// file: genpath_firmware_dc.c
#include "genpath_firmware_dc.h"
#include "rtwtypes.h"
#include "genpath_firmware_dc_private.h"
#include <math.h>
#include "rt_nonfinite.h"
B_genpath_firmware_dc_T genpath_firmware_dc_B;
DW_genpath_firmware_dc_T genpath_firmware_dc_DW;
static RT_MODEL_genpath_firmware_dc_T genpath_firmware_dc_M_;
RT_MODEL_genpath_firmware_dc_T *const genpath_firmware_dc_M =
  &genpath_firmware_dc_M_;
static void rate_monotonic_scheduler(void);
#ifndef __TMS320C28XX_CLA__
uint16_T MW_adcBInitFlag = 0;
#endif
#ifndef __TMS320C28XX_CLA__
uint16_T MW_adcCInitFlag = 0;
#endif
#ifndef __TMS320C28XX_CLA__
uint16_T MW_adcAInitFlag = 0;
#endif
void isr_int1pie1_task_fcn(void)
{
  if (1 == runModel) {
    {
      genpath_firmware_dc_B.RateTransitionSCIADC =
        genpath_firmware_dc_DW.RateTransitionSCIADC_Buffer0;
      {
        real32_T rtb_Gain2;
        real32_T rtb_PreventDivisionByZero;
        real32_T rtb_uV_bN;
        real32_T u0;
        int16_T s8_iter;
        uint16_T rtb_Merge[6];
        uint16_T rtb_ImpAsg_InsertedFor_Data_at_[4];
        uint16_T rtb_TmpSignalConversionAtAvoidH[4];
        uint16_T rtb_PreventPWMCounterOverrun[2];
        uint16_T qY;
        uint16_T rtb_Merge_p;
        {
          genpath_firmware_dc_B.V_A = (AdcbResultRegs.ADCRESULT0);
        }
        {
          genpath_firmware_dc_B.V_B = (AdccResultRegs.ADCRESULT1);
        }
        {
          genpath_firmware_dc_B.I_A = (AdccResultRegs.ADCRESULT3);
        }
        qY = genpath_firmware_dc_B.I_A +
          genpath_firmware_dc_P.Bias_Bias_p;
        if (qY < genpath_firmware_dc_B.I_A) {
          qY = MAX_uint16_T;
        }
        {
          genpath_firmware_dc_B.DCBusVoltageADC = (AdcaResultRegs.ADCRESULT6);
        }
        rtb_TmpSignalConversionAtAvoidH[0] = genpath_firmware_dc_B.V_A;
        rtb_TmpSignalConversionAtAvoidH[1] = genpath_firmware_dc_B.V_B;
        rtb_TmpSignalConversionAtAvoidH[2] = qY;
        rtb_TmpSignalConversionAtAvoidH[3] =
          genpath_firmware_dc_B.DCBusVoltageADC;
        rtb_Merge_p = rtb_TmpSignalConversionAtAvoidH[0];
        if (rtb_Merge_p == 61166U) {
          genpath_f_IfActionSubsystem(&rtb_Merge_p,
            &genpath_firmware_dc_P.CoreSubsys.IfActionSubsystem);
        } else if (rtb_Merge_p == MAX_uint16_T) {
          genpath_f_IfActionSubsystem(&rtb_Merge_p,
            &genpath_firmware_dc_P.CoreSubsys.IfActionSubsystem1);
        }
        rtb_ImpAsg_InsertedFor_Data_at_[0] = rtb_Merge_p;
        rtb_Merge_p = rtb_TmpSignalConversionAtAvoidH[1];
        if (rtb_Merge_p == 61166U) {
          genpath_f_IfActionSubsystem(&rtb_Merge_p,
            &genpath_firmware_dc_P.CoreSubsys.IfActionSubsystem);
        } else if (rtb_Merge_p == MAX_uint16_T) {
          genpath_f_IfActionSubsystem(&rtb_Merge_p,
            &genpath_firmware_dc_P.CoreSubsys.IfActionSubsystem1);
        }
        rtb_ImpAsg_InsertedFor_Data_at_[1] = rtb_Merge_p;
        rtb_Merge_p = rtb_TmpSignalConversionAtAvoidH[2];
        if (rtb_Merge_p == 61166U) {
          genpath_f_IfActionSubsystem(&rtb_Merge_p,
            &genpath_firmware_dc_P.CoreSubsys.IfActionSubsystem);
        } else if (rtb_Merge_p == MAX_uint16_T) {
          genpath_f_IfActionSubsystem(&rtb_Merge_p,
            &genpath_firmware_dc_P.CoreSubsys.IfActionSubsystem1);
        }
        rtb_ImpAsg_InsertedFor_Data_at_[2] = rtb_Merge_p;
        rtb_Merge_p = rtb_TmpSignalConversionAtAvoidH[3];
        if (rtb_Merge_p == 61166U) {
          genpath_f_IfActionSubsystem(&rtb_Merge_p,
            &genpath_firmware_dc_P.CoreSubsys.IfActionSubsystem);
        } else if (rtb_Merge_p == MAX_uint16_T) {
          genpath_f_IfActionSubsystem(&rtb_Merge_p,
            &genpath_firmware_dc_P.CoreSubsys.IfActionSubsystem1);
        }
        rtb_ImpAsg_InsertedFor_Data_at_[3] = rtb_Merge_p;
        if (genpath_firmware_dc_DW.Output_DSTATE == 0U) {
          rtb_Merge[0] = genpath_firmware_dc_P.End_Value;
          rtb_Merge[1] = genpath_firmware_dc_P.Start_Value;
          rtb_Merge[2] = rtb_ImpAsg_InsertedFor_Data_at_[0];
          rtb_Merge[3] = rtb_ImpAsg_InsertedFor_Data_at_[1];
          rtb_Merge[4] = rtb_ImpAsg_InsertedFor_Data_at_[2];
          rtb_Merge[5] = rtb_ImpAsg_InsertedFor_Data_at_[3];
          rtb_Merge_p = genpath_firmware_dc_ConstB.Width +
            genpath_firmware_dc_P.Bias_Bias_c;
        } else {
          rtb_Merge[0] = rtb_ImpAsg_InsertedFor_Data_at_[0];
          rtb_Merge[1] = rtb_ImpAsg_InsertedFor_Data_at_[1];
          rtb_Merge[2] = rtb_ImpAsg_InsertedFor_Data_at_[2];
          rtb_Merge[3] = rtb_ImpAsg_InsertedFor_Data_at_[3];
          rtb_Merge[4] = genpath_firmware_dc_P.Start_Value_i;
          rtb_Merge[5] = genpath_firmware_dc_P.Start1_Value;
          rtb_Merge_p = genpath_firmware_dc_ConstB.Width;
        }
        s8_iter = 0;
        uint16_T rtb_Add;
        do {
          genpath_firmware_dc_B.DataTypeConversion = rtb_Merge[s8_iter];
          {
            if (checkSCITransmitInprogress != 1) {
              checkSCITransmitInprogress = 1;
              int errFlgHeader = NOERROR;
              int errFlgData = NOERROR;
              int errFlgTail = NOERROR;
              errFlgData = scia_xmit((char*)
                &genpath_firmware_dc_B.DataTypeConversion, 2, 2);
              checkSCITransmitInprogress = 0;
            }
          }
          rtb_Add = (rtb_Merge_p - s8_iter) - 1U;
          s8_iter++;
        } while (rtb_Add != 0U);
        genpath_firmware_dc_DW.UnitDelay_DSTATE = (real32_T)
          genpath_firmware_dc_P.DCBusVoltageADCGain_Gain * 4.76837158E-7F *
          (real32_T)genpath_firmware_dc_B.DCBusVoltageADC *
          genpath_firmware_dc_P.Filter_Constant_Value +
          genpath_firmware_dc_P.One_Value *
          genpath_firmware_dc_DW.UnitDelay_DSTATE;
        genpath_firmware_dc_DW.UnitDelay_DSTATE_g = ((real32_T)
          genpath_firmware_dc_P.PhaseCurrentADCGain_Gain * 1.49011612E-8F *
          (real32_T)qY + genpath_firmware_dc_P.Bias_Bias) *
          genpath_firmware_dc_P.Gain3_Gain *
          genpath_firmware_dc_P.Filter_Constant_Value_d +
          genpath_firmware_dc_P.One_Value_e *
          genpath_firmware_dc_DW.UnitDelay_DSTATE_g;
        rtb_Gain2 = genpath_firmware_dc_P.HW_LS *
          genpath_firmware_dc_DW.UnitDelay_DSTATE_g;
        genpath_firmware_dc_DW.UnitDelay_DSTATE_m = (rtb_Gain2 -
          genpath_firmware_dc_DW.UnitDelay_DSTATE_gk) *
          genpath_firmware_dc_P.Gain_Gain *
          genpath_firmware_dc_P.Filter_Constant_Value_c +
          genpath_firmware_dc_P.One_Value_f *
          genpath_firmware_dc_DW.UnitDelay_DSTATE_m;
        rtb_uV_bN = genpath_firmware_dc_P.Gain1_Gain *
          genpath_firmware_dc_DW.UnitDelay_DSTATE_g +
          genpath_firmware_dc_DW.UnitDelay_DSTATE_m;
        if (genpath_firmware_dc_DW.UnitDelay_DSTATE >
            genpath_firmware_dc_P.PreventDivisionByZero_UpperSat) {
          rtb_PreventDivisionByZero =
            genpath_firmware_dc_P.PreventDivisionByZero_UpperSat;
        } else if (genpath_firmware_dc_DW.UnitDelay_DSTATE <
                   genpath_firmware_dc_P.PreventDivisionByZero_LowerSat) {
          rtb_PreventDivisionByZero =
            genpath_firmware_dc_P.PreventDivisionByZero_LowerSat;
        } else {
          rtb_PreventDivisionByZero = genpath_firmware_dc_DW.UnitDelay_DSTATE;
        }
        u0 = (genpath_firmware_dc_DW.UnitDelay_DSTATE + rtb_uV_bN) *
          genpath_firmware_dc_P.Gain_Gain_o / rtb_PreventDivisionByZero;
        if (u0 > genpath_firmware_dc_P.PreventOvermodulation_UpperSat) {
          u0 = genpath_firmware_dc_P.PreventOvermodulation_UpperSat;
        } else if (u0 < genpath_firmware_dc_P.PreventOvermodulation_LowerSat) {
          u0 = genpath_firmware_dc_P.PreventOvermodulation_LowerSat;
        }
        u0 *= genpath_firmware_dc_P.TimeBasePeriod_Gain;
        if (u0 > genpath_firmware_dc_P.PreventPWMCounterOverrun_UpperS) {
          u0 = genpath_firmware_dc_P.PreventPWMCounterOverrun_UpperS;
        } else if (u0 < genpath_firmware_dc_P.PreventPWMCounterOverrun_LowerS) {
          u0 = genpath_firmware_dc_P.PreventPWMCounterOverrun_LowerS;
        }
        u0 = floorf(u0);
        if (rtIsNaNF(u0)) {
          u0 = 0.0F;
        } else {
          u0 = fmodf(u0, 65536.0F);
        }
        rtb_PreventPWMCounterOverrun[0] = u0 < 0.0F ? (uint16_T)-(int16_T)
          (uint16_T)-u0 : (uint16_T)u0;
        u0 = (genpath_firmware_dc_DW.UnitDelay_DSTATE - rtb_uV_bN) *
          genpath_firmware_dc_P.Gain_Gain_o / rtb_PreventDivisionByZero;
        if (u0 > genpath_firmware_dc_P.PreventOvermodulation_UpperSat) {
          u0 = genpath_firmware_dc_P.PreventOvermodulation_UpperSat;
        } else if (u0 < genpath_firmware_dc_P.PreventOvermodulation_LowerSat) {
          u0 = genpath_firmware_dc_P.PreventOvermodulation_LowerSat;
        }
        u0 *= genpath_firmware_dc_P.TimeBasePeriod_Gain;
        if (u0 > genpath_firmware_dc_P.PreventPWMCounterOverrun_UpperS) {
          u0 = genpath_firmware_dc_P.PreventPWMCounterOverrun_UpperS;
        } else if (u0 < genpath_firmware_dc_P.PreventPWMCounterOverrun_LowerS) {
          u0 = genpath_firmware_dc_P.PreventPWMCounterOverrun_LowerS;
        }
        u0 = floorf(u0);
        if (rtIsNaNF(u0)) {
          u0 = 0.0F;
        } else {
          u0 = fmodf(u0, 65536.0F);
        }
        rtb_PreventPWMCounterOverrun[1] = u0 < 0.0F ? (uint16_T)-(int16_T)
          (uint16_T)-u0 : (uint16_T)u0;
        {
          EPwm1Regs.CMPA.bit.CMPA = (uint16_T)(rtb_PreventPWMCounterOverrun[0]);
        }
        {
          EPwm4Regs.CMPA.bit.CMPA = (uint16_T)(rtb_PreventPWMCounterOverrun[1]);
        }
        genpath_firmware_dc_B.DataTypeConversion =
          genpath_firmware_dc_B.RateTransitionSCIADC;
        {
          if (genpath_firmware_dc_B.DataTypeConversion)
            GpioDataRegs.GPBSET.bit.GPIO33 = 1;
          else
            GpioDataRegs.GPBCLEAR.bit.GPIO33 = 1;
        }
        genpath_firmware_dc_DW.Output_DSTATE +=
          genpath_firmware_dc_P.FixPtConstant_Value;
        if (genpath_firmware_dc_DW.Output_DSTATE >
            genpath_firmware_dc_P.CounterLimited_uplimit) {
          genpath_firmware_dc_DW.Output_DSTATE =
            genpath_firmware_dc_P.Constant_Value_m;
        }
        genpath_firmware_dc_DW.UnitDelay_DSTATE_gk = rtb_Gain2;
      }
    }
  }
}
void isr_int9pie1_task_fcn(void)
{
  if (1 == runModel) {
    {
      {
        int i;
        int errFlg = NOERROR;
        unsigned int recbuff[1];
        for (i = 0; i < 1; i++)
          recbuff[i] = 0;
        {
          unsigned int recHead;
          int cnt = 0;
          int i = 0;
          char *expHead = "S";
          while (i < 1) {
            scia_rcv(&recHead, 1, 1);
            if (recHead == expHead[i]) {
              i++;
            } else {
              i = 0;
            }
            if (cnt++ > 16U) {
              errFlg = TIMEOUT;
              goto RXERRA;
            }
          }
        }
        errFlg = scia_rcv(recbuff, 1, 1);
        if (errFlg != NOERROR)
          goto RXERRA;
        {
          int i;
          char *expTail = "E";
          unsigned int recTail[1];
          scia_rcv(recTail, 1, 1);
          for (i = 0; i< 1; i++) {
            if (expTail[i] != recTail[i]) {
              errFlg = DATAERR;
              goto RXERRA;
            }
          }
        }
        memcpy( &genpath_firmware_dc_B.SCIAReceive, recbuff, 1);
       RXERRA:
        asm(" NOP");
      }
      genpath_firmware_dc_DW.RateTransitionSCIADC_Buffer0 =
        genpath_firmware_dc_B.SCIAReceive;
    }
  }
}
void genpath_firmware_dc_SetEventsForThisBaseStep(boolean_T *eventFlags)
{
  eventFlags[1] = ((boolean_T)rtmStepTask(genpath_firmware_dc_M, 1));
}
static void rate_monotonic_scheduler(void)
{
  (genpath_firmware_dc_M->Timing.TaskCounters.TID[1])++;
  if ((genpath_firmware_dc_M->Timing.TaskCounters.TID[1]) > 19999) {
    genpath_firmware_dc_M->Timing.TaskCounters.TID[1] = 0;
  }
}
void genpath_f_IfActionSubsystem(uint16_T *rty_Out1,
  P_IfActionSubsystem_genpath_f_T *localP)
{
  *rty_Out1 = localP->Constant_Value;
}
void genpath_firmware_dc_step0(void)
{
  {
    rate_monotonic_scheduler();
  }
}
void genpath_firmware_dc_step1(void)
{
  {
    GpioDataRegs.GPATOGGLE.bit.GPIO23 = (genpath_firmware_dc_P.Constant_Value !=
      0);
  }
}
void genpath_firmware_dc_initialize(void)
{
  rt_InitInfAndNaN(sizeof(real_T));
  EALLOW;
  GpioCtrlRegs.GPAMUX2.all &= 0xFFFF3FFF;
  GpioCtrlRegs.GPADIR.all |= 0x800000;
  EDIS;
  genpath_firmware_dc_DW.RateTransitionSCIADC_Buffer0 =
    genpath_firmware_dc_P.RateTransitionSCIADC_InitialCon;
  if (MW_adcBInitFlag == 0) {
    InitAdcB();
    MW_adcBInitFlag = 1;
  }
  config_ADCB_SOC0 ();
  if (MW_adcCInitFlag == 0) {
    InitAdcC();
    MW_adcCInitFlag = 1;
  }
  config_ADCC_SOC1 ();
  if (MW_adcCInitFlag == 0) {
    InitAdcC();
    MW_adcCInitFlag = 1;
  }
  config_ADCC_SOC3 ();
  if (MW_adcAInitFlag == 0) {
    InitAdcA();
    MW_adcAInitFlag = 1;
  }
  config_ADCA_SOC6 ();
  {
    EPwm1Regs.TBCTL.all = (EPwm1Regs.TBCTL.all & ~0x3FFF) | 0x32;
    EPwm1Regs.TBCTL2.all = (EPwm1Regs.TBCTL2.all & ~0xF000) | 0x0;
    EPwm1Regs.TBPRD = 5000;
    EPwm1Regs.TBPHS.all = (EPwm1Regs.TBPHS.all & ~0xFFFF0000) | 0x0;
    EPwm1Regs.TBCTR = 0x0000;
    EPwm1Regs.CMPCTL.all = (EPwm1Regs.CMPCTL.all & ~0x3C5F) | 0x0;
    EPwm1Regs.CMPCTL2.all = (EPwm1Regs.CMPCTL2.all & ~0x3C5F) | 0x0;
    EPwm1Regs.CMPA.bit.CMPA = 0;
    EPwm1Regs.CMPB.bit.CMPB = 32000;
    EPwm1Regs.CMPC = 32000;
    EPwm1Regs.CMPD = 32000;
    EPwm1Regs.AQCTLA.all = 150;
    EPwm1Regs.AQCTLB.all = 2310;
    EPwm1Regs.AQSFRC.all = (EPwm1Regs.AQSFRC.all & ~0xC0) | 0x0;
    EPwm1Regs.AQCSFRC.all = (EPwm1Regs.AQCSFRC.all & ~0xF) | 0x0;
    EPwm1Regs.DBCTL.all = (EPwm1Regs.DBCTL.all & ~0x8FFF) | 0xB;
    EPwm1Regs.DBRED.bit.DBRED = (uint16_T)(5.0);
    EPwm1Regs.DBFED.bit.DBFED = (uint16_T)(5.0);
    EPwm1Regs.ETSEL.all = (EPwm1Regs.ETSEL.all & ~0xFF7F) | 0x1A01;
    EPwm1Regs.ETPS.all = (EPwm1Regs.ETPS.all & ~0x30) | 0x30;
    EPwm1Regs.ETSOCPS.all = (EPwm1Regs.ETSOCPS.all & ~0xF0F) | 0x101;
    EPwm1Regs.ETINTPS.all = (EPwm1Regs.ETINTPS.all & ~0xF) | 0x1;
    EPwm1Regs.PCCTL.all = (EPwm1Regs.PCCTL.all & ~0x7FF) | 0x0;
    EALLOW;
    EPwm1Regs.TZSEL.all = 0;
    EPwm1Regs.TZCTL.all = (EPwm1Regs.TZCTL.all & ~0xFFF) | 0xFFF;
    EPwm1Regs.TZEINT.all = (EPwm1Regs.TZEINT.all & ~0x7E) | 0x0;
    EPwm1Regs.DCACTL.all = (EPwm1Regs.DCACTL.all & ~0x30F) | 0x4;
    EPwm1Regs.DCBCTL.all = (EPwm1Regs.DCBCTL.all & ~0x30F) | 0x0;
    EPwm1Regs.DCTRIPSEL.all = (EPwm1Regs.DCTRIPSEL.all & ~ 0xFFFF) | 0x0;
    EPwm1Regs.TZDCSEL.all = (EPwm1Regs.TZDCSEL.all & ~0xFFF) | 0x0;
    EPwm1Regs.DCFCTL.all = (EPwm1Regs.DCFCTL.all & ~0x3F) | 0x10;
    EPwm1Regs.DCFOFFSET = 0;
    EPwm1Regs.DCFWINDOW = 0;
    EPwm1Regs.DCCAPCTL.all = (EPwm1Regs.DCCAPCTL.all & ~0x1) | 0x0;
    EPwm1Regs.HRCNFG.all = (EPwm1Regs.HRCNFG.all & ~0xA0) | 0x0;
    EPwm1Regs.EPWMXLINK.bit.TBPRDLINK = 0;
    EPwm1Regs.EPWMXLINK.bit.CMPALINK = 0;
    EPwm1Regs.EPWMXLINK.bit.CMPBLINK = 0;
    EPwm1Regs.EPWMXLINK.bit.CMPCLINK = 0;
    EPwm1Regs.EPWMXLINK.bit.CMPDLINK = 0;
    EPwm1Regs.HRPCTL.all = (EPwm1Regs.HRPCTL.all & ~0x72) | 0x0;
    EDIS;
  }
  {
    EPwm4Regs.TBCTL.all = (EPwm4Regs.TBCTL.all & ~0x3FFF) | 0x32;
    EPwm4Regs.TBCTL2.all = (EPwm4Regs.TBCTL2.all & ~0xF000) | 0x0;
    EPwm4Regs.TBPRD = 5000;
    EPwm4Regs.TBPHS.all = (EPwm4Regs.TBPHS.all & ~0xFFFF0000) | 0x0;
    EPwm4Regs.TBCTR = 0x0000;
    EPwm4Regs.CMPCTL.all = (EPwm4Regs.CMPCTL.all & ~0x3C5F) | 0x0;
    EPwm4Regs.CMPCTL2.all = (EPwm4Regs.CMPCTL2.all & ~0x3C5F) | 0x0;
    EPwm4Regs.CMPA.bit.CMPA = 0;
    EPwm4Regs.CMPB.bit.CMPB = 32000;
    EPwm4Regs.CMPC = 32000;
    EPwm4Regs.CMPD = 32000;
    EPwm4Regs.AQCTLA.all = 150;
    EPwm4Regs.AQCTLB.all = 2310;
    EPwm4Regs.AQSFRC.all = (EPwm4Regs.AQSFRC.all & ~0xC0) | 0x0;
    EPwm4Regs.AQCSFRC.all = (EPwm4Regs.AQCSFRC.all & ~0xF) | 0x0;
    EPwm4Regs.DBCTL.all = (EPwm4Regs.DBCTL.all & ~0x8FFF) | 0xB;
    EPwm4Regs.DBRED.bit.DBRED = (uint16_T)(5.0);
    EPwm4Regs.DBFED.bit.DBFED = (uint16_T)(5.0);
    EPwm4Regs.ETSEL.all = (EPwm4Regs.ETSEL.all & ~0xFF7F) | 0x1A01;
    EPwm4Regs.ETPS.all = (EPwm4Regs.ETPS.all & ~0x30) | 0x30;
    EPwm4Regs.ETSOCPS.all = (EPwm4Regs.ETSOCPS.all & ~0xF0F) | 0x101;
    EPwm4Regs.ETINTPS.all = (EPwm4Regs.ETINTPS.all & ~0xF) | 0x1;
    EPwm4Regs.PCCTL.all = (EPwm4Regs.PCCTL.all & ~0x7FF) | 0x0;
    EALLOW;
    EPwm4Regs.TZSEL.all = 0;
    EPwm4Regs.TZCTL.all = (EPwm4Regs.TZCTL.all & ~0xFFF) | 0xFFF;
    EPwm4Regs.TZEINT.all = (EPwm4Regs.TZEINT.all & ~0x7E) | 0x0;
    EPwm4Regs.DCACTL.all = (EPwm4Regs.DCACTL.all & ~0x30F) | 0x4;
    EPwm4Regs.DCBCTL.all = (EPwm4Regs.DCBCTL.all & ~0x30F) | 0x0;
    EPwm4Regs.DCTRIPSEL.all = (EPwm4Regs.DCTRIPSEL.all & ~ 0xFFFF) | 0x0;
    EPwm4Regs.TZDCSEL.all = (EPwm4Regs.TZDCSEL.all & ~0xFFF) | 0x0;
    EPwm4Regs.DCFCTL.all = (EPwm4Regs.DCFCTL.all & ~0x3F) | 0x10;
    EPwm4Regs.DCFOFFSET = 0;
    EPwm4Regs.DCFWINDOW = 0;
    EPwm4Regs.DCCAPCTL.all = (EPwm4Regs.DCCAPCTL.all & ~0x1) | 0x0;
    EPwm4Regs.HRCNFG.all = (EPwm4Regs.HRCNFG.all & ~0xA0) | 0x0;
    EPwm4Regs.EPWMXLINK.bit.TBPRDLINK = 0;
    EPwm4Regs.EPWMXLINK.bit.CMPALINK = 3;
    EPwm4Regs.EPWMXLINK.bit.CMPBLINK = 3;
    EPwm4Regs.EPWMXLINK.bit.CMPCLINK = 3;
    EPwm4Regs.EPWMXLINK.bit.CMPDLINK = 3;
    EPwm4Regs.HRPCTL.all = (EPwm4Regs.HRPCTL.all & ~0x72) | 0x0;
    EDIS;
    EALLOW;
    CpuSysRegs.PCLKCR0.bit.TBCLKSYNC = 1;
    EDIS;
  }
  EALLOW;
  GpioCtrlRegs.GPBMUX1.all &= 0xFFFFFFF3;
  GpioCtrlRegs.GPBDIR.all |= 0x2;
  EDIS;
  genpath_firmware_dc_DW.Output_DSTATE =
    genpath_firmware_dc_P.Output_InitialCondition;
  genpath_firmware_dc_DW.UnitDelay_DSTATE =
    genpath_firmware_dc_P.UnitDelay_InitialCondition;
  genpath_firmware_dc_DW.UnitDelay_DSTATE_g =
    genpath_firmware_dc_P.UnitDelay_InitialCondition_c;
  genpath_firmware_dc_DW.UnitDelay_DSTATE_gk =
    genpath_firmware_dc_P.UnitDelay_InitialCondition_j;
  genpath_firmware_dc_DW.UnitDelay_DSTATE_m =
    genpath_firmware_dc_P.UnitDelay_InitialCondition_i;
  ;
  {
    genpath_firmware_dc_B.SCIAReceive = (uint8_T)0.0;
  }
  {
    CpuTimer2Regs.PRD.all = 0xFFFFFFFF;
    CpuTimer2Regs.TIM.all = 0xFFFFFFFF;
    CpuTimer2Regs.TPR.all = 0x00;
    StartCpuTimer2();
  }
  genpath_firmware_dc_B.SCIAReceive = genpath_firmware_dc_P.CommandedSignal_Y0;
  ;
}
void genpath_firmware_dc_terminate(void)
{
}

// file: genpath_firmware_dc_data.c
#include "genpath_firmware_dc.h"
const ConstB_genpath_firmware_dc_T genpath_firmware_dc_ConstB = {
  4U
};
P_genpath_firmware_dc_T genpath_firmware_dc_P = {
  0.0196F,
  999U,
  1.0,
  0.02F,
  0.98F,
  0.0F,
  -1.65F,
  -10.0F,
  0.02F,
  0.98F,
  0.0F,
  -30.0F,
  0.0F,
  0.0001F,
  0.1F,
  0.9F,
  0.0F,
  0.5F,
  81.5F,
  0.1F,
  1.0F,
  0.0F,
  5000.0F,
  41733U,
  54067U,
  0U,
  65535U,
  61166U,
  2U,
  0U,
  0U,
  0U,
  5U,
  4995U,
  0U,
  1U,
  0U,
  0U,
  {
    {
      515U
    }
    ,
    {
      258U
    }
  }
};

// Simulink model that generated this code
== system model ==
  Subsystem#1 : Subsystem  <- 1: RateTransitionSCIADC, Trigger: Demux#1
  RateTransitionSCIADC : RateTransition  <- 1: Subsystem#2
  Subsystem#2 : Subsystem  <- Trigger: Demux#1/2
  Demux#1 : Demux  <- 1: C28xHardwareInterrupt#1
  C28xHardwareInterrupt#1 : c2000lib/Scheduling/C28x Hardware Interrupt
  DigitalOutput#1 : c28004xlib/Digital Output  <- 1: Constant
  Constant : Constant
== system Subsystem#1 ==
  CommandedSignal : Inport
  TriggerPort#1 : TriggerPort  TriggerType=function-call
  IIRFilter#1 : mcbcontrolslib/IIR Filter  <- 1: Gain#1
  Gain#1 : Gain  Gain=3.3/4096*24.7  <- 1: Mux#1
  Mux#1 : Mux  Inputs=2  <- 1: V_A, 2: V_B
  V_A : c2802xlib/ADC
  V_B : c2802xlib/ADC
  Subsystem#3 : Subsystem  <- 1: Merge, 2: Merge#1
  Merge : Merge  <- 1: Start, 2: Data
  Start : Subsystem  <- 1: Subsystem#4, 2: Width, Action: If#1
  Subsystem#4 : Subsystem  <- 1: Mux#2
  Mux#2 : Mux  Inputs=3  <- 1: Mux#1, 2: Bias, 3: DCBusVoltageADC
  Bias : Bias  Bias=+5  <- 1: I_A
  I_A : c2802xlib/ADC
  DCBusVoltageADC : c2802xlib/ADC
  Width : Width  <- 1: Subsystem#4
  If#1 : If  IfExpression=u1 == 0  <- 1: CounterLimited
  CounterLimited : simulink/Sources/Counter Limited  uplimit=999
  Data : Subsystem  <- 1: Subsystem#4, 2: Width, Action: If#1/2
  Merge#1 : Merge  <- 1: Start/2, 2: Data/2
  ePWM#1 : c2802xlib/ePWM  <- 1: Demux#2
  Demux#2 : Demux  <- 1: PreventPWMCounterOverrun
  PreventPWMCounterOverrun : Saturate  UpperLimit=4995  LowerLimit=0  <- 1: TimeBasePeriod
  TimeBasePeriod : Gain  Gain=5000  <- 1: PreventOvermodulation
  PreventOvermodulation : Saturate  UpperLimit=1  LowerLimit=0  <- 1: Product#1
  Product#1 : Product  Inputs=*/  <- 1: Gain, 2: PreventDivisionByZero
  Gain : Gain  Gain=1/2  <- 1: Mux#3
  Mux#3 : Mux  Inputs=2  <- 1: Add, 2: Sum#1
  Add : Sum  <- 1: IIRFilter#2, 2: Sum#2
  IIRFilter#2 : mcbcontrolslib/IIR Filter  <- 1: DCBusVoltageADCGain
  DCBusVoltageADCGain : Gain  Gain=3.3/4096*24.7  <- 1: DCBusVoltageADC
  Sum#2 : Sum  Inputs=++  <- 1: Gain1, 2: IIRFilter#3
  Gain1 : Gain  Gain=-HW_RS  <- 1: IIRFilter#4
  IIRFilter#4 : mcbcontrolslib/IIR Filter  <- 1: Gain3
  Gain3 : Gain  Gain=-10  <- 1: Bias#1
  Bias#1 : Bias  Bias=-1.65  <- 1: PhaseCurrentADCGain
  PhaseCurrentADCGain : Gain  Gain=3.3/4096  <- 1: Bias
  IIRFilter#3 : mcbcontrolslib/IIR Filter  <- 1: Gain#2
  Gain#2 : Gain  Gain=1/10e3  <- 1: Sum#3
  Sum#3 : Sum  Inputs=+-  <- 1: Gain2, 2: UnitDelay
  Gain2 : Gain  Gain=HW_LS  <- 1: IIRFilter#4
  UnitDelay : UnitDelay  <- 1: Gain2
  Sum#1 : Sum  Inputs=+-  <- 1: IIRFilter#2, 2: Sum#2
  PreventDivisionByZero : Saturate  UpperLimit=81.5  LowerLimit=0.1  <- 1: IIRFilter#2
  ePWM#2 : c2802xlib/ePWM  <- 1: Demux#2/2
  DigitalOutput#2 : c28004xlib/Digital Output  <- 1: DataTypeConversion
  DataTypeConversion : DataTypeConversion  <- 1: CommandedSignal
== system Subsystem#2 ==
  TriggerPort#2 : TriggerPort  TriggerType=function-call
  Outport#1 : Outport  <- 1: SCIAReceive
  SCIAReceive : c280xlib/SCI Receive
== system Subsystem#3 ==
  Inport#1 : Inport
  Inport#2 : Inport
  WhileIterator#1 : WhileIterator  MaxIters=-1  WhileBlockType=do-while  <- 1: Sum#4
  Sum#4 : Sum  Inputs=+-  <- 1: Inport#2, 2: WhileIterator#1
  SCITransmit#1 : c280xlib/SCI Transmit  <- 1: MultiPortSwitch#1
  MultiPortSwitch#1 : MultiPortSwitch  Inputs=1  <- 1: WhileIterator#1, 2: Inport#1
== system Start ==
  Inport#3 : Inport
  Inport#4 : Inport
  ActionPort#1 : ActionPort
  Outport#2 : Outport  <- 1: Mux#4
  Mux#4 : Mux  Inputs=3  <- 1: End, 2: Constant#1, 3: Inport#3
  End : Constant  Value=65535
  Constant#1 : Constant  Value=61166
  Outport#3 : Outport  <- 1: Bias#2
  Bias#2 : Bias  Bias=2  <- 1: Inport#4
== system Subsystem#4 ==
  Inport#5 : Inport
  ForEach#1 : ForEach
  Outport#4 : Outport  <- 1: Merge#2
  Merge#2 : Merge  Inputs=3  <- 1: IfActionSubsystem, 2: IfActionSubsystem1, 3: Subsystem#5
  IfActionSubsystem : Subsystem  <- Action: If#2
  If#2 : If  IfExpression=u1 == 61166  ElseIfExpressions=u1 == 65535  <- 1: Inport#5
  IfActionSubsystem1 : Subsystem  <- Action: If#2/2
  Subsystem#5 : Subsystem  <- 1: Inport#5, Action: If#2/3
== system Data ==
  Inport#6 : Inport
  Inport#7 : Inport
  ActionPort#2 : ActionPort
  Outport#5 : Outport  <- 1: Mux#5
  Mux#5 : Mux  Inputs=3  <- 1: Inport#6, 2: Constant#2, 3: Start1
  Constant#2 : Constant  Value=0
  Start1 : Constant  Value=0
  Outport#6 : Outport  <- 1: Inport#7
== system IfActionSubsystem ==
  ActionPort#3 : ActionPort
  Out1 : Outport  <- 1: Constant#3
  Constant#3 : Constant  Value=258
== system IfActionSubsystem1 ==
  ActionPort#4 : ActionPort
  Outport#7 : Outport  <- 1: Constant#4
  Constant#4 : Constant  Value=515
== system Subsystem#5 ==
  Inport#8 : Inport
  ActionPort#5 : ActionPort
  Outport#8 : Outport  <- 1: Inport#8
